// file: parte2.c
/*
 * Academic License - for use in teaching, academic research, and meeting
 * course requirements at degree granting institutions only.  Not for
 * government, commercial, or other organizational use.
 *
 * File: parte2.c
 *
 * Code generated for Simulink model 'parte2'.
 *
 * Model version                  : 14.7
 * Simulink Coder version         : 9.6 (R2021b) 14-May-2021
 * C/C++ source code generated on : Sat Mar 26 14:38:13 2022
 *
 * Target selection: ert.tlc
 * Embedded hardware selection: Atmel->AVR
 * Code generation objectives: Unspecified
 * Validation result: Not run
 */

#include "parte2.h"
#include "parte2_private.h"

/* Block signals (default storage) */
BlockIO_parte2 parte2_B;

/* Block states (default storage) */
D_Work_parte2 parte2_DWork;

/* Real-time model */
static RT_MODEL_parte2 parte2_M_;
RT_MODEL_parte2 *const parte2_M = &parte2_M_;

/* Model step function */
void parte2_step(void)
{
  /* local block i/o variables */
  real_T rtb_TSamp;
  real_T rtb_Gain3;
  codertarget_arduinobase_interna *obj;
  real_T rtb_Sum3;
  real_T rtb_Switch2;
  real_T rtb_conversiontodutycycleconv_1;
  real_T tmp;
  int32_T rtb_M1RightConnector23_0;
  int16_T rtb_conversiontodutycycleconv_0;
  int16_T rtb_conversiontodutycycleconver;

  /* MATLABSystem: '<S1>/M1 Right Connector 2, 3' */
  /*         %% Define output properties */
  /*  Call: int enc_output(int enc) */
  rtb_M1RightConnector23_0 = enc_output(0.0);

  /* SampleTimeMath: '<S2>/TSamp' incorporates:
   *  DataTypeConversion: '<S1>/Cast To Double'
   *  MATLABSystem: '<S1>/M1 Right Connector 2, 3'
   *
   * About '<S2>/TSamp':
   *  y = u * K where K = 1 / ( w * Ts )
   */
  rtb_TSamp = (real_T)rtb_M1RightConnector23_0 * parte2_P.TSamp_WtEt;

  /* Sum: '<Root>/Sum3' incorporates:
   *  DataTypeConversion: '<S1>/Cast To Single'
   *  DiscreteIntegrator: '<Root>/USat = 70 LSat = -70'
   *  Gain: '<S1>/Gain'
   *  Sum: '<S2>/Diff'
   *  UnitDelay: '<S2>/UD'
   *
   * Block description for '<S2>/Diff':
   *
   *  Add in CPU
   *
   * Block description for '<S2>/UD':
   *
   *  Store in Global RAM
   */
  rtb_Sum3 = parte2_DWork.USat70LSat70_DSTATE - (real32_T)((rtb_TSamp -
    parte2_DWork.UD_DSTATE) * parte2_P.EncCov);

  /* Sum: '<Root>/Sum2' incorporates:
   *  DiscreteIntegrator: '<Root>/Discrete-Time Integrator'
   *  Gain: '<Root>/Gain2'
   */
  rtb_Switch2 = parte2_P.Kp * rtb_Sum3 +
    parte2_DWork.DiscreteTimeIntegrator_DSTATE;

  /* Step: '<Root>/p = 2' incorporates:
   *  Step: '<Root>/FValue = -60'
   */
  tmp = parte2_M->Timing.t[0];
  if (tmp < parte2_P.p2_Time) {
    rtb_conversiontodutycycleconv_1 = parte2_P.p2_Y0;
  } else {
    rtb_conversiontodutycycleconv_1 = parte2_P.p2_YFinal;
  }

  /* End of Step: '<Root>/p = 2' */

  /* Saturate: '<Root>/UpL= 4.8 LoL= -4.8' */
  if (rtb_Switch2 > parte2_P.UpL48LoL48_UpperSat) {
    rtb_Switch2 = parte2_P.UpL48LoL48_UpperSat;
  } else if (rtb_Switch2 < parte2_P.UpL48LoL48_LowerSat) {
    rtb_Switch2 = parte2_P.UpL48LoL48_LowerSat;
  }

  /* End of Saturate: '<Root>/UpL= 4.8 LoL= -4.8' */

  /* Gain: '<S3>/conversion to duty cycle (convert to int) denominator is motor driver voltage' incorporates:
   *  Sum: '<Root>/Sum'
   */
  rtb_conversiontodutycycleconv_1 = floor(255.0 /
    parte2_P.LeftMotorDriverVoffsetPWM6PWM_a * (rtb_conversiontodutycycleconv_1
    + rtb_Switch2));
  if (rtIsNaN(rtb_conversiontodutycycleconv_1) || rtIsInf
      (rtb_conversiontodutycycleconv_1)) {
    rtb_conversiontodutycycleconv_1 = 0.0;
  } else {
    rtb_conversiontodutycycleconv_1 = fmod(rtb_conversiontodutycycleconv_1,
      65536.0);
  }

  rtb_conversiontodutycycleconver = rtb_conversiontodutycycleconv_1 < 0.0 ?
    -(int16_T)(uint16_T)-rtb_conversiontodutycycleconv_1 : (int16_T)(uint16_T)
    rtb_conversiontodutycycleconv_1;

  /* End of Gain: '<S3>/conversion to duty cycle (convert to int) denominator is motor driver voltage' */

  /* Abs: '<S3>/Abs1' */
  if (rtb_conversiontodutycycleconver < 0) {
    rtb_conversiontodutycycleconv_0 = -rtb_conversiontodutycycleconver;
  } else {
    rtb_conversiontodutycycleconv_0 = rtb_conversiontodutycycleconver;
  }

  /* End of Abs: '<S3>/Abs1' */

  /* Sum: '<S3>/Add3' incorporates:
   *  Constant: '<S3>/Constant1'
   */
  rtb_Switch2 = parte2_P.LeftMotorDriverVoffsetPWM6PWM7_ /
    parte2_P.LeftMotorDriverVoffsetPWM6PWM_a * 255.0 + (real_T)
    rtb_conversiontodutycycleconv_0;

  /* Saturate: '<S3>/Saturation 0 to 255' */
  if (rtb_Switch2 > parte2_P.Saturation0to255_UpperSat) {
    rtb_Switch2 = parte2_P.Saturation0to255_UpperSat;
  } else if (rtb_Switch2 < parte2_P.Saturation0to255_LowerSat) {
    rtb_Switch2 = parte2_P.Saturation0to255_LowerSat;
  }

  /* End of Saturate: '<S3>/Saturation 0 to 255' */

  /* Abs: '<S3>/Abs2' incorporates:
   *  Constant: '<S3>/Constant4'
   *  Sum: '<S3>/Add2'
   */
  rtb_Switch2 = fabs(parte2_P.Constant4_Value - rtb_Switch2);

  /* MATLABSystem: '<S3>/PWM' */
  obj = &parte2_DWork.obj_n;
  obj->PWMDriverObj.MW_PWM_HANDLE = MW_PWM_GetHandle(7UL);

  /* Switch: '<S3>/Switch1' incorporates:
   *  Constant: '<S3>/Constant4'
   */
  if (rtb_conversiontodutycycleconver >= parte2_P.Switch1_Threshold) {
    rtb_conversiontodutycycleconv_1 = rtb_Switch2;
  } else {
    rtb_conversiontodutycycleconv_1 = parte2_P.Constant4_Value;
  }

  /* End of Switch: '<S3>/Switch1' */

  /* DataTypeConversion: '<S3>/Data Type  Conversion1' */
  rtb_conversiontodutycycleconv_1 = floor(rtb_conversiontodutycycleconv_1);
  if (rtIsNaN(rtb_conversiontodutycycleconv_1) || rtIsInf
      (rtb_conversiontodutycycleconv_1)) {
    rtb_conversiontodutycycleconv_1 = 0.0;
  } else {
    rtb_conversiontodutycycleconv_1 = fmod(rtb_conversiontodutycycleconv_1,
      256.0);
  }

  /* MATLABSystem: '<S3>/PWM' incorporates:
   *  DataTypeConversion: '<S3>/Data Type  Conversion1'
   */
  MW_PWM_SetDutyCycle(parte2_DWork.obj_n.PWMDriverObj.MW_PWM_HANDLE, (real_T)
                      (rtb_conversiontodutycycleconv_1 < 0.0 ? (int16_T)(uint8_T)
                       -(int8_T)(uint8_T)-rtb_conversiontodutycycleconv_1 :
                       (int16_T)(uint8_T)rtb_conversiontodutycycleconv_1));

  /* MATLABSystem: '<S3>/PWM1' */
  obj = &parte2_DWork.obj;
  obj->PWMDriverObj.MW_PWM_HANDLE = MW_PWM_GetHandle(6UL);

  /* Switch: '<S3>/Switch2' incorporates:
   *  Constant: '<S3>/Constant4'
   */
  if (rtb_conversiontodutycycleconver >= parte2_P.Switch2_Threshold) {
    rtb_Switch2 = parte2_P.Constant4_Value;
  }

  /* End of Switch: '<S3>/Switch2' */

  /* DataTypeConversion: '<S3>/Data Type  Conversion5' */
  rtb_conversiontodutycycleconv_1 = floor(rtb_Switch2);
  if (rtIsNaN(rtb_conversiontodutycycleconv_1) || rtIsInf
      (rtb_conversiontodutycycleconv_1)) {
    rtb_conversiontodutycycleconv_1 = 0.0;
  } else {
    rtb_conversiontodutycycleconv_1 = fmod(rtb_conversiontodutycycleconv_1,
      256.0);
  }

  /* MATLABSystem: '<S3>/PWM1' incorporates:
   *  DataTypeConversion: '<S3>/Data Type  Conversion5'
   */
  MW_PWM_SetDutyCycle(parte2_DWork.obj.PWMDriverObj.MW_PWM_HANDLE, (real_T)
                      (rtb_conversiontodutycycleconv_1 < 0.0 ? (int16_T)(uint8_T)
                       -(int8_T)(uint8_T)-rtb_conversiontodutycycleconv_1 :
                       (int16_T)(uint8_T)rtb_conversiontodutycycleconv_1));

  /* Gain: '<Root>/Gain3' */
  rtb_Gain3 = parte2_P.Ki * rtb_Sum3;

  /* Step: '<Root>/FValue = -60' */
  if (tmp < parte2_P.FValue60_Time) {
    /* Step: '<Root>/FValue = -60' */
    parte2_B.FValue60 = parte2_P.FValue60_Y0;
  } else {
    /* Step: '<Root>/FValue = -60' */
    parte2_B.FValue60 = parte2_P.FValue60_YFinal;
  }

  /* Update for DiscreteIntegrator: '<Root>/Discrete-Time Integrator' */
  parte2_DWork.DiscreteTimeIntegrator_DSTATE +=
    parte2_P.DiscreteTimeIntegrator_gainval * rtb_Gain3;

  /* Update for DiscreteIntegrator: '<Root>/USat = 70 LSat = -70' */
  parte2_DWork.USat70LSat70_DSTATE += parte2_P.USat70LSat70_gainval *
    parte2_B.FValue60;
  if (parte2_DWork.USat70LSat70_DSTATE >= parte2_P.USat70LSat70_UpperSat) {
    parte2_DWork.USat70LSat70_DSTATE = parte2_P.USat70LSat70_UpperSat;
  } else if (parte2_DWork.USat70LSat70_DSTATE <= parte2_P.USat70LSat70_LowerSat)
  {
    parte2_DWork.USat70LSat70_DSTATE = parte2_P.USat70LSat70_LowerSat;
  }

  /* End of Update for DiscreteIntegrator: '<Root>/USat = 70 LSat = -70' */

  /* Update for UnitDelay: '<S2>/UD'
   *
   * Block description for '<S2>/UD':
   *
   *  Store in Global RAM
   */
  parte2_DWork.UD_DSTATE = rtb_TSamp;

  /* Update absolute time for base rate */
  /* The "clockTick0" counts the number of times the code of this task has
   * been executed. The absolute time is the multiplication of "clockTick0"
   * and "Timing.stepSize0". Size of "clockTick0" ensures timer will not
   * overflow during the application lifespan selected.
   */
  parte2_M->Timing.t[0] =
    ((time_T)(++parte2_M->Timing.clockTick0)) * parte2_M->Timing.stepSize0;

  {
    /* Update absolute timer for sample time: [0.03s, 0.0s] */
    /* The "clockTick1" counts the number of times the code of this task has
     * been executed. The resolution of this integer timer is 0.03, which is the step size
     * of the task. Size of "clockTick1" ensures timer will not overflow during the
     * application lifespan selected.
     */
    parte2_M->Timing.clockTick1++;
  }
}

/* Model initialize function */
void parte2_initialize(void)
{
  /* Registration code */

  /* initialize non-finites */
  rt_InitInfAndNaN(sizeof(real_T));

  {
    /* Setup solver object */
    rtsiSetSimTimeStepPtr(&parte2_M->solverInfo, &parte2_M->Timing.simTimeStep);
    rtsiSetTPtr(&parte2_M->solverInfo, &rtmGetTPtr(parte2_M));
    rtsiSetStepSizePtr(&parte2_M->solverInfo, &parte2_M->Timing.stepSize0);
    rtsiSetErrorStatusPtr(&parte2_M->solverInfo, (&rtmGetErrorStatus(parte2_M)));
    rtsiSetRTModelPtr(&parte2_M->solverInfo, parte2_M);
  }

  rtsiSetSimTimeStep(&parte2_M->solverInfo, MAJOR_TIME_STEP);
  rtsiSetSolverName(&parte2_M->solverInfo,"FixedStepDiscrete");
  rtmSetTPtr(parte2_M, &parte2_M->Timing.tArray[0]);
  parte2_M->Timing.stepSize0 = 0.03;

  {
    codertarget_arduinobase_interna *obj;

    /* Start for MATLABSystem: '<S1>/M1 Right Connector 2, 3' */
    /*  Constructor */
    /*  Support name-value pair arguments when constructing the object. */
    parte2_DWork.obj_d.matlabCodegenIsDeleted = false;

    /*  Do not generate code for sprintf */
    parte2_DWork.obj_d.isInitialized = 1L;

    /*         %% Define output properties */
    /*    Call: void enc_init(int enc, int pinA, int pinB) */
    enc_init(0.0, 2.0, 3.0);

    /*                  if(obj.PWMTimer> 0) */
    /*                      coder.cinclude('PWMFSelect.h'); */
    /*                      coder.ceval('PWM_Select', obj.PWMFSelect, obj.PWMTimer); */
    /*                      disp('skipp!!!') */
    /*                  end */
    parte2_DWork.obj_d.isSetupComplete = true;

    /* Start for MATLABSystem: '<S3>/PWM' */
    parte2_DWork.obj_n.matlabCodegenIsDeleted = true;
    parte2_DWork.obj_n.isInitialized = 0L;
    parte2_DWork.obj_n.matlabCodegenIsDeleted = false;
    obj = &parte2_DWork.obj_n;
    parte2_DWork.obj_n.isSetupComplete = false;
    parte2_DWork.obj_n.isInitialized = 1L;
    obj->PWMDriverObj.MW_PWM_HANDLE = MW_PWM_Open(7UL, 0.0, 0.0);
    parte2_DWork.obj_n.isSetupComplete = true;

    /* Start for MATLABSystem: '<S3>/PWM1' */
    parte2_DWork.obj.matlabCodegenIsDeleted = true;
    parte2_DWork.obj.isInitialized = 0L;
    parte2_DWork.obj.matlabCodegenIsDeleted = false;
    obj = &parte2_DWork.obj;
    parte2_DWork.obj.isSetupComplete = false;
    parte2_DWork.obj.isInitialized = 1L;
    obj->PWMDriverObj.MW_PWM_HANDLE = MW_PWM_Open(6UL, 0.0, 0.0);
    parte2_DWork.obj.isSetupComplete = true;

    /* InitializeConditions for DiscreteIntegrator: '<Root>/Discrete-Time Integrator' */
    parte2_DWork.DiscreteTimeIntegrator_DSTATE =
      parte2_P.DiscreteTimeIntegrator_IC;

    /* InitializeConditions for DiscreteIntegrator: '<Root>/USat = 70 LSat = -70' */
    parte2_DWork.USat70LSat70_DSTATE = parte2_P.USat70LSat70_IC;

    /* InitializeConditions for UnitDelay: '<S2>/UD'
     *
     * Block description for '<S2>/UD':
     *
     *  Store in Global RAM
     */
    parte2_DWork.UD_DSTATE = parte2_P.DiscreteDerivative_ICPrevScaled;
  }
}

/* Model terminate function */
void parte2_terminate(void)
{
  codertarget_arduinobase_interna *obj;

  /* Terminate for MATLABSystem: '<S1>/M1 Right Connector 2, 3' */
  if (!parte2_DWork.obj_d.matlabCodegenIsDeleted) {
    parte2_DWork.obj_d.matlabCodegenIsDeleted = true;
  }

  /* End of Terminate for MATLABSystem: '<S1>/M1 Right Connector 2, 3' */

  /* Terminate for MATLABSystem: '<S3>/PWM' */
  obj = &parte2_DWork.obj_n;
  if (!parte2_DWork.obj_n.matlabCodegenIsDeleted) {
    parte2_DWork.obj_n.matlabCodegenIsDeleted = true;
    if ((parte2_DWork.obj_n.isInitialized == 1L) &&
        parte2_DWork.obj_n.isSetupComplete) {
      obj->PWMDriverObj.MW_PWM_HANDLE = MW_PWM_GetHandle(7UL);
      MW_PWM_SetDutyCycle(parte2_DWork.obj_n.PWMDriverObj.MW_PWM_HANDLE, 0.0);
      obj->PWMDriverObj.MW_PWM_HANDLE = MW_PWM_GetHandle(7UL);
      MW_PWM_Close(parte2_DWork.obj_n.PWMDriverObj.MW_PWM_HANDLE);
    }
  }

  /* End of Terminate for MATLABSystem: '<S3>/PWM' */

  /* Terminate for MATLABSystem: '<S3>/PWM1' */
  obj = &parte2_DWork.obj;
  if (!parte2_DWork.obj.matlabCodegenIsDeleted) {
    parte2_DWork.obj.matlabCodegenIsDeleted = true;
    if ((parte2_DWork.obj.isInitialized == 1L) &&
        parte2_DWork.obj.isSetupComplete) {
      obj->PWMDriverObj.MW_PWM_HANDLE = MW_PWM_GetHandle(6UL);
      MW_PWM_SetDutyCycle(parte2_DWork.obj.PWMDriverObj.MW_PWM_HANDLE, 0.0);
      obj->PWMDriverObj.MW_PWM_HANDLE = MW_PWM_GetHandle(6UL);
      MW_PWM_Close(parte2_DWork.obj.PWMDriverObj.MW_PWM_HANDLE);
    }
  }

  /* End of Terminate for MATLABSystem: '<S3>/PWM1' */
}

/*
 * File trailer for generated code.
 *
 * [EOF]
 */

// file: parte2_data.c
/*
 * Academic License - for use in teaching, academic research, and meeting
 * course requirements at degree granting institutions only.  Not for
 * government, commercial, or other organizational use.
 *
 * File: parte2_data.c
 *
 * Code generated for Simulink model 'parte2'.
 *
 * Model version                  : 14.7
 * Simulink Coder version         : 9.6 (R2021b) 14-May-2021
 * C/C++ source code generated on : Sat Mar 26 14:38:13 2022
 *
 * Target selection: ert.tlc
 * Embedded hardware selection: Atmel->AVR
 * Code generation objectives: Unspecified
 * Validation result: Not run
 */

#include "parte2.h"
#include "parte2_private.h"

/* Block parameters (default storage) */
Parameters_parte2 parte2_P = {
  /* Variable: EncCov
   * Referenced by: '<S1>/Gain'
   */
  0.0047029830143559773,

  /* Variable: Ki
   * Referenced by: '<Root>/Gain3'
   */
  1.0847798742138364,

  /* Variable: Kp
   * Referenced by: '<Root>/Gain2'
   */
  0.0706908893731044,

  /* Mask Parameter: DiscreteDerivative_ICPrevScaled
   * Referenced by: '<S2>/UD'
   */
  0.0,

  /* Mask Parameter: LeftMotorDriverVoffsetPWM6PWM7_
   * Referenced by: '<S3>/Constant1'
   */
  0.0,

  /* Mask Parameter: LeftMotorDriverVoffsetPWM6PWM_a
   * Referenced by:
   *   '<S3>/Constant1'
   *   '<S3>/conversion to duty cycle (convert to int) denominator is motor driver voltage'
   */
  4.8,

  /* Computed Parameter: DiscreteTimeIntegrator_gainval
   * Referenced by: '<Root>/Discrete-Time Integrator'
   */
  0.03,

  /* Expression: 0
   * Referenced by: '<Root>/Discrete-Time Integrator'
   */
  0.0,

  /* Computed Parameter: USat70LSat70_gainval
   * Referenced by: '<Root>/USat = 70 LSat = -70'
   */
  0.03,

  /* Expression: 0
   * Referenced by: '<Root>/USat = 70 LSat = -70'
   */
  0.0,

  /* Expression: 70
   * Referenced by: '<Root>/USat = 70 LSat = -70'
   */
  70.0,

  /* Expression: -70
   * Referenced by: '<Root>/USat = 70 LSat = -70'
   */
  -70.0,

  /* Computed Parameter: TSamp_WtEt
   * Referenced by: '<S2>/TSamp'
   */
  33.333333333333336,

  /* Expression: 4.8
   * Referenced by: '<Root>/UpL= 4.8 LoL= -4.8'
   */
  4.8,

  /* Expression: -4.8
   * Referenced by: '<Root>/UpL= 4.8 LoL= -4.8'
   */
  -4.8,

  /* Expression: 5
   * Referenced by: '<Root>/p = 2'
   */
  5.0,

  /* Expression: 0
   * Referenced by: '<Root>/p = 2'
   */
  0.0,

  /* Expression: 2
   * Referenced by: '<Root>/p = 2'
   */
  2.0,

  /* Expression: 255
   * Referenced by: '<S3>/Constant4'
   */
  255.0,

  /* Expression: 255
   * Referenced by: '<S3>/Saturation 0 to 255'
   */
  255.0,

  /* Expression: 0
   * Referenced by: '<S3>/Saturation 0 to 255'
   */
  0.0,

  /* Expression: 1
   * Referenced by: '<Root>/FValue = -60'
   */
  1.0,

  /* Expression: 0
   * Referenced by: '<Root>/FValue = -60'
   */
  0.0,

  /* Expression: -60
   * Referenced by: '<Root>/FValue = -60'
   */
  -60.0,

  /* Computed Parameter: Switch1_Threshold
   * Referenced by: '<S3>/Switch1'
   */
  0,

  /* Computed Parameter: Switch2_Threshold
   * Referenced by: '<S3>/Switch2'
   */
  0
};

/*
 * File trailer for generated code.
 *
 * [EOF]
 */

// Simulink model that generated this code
simulink model "parte2"  (R2021b)
settings: Solver=FixedStepDiscrete  StartTime=0.0  StopTime=6  FixedStep=.03  RelTol=1e-3  EnableMultiTasking=on
PostLoadFcn:
  | try,
  | codertarget.arduinobase.registry.setBaudRate(gcs,115200)
  | disp('baud rate set to 115200 for external mode hardware serial')
  | baudrate='set_to_115200'
  | catch
  | disp('baud rate setting not needed in this version')
  | end
values from neighbouring files (symbols this model uses):
  EncCov = 2*pi /1336    (= 0.00470298301436)    [parte2_script.m]
  h = 0.03    [parte2_script.m]
  Ki = 0.2712    [parte2_script.m]
  Kp = 0.0271    [parte2_script.m]
undefined symbols (not defined in the file or in its folder): DiscIntNeverNeededParam
libraries: MinSegLibrary_M2V5 x2, simulink x1

== system parte2 ==
  Discrete-Time Integrator : DiscreteIntegrator  SampleTime=h  ICPrevOutput=DiscIntNeverNeededParam  ICPrevScaledInput=DiscIntNeverNeededParam
  FValue = -60 : Step  After=-60  SampleTime=0
  Gain2 : Gain  Gain=Kp
  Gain3 : Gain  Gain=Ki
  MotorDC Hardware : Subsystem
  Scope : Scope  NumInputPorts=3
  Sum : Sum  Inputs=++|
  Sum2 : Sum  Inputs=+|+
  Sum3 : Sum  Inputs=|+-
  USat = 70 LSat = -70 : DiscreteIntegrator  SampleTime=h  LimitOutput=on  UpperSaturationLimit=70  LowerSaturationLimit=-70  ICPrevOutput=DiscIntNeverNeededParam  ICPrevScaledInput=DiscIntNeverNeededParam
  UpL= 4.8 LoL= -4.8 : Saturate  UpperLimit=4.8  LowerLimit=-4.8
  p = 2 : Step  Time=5  After=2  SampleTime=0
  wires:
  Sum3/1 -> Gain3/1, Gain2/1
  MotorDC Hardware/1(W) -> Sum3/2, Scope/3  "W"
  FValue = -60/1 -> USat = 70 LSat = -70/1
  Gain2/1 -> Sum2/1
  Gain3/1 -> Discrete-Time Integrator/1
  Sum2/1 -> UpL= 4.8 LoL= -4.8/1
  USat = 70 LSat = -70/1 -> Scope/1, Sum3/1  "ref"
  Discrete-Time Integrator/1 -> Sum2/2
  Sum/1 -> Scope/2, MotorDC Hardware/1(Volts)  "U"
  UpL= 4.8 LoL= -4.8/1 -> Sum/2
  p = 2/1 -> Sum/1

== system parte2/MotorDC Hardware ==
  Volts : Inport
  Cast To Double : DataTypeConversion  OutDataTypeStr=double
  Cast To Single : DataTypeConversion  OutDataTypeStr=single
  Cast To Single1 : DataTypeConversion  OutDataTypeStr=single
  Discrete Derivative : simulink/Discrete/Discrete Derivative  gainval=1.0  ICPrevScaledInput=0.0  OutMin=[]  OutMax=[]  OutDataType=fixdt(1, 16)  OutScaling=2^-10  DoSatur=off
  Gain : Gain  Gain=EncCov
  Gain1 : Gain  Gain=EncCov
  "Left Motor Driver Voffset PWM6, PWM7" : MinSegLibrary_M2V5/Left Motor Driver Voffset PWM6, PWM7  Vsupply=4.8  Voffset=0
  "M1 Right Connector 2, 3" : MinSegLibrary_M2V5/M1 Right Connector 2, 3  Encoder=0  PinA=2  PinB=3
  W : Outport
  theta : Outport  Port=2
  wires:
  Cast To Single/1 -> W/1
  Gain1/1 -> Cast To Single1/1
  Cast To Single1/1 -> theta/1
  "M1 Right Connector 2, 3"/1 -> Cast To Double/1
  Cast To Double/1 -> Gain1/1, Discrete Derivative/1
  Volts/1 -> "Left Motor Driver Voffset PWM6, PWM7"/1
  Discrete Derivative/1 -> Gain/1
  Gain/1 -> Cast To Single/1
